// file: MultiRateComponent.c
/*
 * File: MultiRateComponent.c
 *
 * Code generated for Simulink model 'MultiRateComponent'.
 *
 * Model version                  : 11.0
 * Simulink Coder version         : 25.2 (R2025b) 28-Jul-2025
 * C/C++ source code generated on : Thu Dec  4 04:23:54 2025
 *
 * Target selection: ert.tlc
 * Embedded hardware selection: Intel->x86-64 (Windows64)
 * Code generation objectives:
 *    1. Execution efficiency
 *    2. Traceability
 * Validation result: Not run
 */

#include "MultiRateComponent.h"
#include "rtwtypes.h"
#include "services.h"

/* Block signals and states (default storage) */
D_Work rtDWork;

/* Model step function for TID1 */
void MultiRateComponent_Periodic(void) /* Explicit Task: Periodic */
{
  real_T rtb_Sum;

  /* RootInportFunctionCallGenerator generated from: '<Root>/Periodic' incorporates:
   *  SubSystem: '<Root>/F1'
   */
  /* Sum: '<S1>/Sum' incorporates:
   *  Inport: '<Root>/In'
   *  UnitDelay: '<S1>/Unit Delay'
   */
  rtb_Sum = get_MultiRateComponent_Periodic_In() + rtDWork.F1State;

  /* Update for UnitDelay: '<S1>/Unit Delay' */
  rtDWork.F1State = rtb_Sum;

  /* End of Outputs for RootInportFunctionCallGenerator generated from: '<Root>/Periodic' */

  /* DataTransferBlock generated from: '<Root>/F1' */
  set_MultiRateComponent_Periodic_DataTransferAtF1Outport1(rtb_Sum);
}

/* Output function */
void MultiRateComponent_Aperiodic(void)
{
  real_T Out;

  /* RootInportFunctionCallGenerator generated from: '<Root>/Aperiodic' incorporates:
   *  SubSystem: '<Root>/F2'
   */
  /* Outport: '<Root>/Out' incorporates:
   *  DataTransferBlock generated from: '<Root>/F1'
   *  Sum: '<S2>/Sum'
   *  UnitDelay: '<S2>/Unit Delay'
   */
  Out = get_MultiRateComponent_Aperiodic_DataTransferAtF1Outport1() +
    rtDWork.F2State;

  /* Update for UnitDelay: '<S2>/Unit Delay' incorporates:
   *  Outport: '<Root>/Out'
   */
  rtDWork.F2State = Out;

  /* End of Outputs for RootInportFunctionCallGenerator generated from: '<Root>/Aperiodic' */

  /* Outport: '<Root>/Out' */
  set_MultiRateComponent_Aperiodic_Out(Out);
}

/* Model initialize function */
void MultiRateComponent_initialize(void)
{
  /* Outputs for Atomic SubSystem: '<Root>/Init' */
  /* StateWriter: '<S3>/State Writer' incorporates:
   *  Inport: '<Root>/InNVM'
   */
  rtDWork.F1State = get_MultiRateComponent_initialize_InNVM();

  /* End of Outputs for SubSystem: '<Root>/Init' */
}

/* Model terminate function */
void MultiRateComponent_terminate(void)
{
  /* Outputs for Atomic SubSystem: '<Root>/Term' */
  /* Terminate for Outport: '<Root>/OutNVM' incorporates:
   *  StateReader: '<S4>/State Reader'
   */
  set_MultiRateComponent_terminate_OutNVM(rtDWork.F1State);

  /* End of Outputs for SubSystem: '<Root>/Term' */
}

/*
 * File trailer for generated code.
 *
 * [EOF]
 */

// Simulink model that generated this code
simulink model "MultiRateComponent"  (R2025b)
settings: Solver=FixedStepDiscrete  StartTime=0.0  StopTime=0.025  MaxStep=.0001  RelTol=1e-3  EnableMultiTasking=on

== system MultiRateComponent ==
  InNVM : Inport
  Periodic : Inport  Port=2  SampleTime=0.001  OutputFunctionCall=on
  In : Inport  Port=3
  Aperiodic : Inport  Port=4  OutputFunctionCall=on
  F1 : Subsystem  TreatAsAtomicUnit=on  RTWFcnName=foo
  F2 : Subsystem  TreatAsAtomicUnit=on  RTWFcnName=foo
  Init : Subsystem  TreatAsAtomicUnit=on  RTWFcnName=foo
  Term : Subsystem  TreatAsAtomicUnit=on  RTWFcnName=foo
  OutNVM : Outport
  Out : Outport  Port=2
  wires:
  Periodic/1 -> F1/Trigger
  InNVM/1 -> Init/1(In1)
  Term/1(Out1) -> OutNVM/1
  F2/1(Out) -> Out/1
  Aperiodic/1 -> F2/Trigger
  In/1 -> F1/1(In)
  F1/1(Out) -> F2/1(In)

== system MultiRateComponent/F1 ==
  In : Inport
  f1 : TriggerPort  TriggerType=function-call  VariantControl=Variant  PortDimensions=1
  Sum : Sum  Inputs=|++
  Unit Delay : UnitDelay  SampleTime=-1  StateName=F1State  HasFrameUpgradeWarning=on
  Out : Outport
  wires:
  In/1 -> Sum/1
  Unit Delay/1 -> Sum/2
  Sum/1 -> Unit Delay/1, Out/1

== system MultiRateComponent/F2 ==
  In : Inport
  f2 : TriggerPort  TriggerType=function-call  VariantControl=Variant  PortDimensions=1
  Sum : Sum  Inputs=|++
  Unit Delay : UnitDelay  SampleTime=-1  StateName=F2State  HasFrameUpgradeWarning=on
  Out : Outport
  wires:
  In/1 -> Sum/1
  Unit Delay/1 -> Sum/2
  Sum/1 -> Out/1, Unit Delay/1

== system MultiRateComponent/Init ==
  In1 : Inport
  Event Listener : EventListener  DisableCoverage=on  EventName=reset
  State Writer : StateWriter  StateOwnerBlock=../../F1/Unit Delay  StateName=F1State
  wires:
  In1/1 -> State Writer/1

== system MultiRateComponent/Term ==
  Event Listener : EventListener  DisableCoverage=on  EventType=Terminate  EventName=reset
  State Reader : StateReader  StateOwnerBlock=../../F1/Unit Delay  StateName=F1State
  Out1 : Outport
  wires:
  State Reader/1 -> Out1/1
